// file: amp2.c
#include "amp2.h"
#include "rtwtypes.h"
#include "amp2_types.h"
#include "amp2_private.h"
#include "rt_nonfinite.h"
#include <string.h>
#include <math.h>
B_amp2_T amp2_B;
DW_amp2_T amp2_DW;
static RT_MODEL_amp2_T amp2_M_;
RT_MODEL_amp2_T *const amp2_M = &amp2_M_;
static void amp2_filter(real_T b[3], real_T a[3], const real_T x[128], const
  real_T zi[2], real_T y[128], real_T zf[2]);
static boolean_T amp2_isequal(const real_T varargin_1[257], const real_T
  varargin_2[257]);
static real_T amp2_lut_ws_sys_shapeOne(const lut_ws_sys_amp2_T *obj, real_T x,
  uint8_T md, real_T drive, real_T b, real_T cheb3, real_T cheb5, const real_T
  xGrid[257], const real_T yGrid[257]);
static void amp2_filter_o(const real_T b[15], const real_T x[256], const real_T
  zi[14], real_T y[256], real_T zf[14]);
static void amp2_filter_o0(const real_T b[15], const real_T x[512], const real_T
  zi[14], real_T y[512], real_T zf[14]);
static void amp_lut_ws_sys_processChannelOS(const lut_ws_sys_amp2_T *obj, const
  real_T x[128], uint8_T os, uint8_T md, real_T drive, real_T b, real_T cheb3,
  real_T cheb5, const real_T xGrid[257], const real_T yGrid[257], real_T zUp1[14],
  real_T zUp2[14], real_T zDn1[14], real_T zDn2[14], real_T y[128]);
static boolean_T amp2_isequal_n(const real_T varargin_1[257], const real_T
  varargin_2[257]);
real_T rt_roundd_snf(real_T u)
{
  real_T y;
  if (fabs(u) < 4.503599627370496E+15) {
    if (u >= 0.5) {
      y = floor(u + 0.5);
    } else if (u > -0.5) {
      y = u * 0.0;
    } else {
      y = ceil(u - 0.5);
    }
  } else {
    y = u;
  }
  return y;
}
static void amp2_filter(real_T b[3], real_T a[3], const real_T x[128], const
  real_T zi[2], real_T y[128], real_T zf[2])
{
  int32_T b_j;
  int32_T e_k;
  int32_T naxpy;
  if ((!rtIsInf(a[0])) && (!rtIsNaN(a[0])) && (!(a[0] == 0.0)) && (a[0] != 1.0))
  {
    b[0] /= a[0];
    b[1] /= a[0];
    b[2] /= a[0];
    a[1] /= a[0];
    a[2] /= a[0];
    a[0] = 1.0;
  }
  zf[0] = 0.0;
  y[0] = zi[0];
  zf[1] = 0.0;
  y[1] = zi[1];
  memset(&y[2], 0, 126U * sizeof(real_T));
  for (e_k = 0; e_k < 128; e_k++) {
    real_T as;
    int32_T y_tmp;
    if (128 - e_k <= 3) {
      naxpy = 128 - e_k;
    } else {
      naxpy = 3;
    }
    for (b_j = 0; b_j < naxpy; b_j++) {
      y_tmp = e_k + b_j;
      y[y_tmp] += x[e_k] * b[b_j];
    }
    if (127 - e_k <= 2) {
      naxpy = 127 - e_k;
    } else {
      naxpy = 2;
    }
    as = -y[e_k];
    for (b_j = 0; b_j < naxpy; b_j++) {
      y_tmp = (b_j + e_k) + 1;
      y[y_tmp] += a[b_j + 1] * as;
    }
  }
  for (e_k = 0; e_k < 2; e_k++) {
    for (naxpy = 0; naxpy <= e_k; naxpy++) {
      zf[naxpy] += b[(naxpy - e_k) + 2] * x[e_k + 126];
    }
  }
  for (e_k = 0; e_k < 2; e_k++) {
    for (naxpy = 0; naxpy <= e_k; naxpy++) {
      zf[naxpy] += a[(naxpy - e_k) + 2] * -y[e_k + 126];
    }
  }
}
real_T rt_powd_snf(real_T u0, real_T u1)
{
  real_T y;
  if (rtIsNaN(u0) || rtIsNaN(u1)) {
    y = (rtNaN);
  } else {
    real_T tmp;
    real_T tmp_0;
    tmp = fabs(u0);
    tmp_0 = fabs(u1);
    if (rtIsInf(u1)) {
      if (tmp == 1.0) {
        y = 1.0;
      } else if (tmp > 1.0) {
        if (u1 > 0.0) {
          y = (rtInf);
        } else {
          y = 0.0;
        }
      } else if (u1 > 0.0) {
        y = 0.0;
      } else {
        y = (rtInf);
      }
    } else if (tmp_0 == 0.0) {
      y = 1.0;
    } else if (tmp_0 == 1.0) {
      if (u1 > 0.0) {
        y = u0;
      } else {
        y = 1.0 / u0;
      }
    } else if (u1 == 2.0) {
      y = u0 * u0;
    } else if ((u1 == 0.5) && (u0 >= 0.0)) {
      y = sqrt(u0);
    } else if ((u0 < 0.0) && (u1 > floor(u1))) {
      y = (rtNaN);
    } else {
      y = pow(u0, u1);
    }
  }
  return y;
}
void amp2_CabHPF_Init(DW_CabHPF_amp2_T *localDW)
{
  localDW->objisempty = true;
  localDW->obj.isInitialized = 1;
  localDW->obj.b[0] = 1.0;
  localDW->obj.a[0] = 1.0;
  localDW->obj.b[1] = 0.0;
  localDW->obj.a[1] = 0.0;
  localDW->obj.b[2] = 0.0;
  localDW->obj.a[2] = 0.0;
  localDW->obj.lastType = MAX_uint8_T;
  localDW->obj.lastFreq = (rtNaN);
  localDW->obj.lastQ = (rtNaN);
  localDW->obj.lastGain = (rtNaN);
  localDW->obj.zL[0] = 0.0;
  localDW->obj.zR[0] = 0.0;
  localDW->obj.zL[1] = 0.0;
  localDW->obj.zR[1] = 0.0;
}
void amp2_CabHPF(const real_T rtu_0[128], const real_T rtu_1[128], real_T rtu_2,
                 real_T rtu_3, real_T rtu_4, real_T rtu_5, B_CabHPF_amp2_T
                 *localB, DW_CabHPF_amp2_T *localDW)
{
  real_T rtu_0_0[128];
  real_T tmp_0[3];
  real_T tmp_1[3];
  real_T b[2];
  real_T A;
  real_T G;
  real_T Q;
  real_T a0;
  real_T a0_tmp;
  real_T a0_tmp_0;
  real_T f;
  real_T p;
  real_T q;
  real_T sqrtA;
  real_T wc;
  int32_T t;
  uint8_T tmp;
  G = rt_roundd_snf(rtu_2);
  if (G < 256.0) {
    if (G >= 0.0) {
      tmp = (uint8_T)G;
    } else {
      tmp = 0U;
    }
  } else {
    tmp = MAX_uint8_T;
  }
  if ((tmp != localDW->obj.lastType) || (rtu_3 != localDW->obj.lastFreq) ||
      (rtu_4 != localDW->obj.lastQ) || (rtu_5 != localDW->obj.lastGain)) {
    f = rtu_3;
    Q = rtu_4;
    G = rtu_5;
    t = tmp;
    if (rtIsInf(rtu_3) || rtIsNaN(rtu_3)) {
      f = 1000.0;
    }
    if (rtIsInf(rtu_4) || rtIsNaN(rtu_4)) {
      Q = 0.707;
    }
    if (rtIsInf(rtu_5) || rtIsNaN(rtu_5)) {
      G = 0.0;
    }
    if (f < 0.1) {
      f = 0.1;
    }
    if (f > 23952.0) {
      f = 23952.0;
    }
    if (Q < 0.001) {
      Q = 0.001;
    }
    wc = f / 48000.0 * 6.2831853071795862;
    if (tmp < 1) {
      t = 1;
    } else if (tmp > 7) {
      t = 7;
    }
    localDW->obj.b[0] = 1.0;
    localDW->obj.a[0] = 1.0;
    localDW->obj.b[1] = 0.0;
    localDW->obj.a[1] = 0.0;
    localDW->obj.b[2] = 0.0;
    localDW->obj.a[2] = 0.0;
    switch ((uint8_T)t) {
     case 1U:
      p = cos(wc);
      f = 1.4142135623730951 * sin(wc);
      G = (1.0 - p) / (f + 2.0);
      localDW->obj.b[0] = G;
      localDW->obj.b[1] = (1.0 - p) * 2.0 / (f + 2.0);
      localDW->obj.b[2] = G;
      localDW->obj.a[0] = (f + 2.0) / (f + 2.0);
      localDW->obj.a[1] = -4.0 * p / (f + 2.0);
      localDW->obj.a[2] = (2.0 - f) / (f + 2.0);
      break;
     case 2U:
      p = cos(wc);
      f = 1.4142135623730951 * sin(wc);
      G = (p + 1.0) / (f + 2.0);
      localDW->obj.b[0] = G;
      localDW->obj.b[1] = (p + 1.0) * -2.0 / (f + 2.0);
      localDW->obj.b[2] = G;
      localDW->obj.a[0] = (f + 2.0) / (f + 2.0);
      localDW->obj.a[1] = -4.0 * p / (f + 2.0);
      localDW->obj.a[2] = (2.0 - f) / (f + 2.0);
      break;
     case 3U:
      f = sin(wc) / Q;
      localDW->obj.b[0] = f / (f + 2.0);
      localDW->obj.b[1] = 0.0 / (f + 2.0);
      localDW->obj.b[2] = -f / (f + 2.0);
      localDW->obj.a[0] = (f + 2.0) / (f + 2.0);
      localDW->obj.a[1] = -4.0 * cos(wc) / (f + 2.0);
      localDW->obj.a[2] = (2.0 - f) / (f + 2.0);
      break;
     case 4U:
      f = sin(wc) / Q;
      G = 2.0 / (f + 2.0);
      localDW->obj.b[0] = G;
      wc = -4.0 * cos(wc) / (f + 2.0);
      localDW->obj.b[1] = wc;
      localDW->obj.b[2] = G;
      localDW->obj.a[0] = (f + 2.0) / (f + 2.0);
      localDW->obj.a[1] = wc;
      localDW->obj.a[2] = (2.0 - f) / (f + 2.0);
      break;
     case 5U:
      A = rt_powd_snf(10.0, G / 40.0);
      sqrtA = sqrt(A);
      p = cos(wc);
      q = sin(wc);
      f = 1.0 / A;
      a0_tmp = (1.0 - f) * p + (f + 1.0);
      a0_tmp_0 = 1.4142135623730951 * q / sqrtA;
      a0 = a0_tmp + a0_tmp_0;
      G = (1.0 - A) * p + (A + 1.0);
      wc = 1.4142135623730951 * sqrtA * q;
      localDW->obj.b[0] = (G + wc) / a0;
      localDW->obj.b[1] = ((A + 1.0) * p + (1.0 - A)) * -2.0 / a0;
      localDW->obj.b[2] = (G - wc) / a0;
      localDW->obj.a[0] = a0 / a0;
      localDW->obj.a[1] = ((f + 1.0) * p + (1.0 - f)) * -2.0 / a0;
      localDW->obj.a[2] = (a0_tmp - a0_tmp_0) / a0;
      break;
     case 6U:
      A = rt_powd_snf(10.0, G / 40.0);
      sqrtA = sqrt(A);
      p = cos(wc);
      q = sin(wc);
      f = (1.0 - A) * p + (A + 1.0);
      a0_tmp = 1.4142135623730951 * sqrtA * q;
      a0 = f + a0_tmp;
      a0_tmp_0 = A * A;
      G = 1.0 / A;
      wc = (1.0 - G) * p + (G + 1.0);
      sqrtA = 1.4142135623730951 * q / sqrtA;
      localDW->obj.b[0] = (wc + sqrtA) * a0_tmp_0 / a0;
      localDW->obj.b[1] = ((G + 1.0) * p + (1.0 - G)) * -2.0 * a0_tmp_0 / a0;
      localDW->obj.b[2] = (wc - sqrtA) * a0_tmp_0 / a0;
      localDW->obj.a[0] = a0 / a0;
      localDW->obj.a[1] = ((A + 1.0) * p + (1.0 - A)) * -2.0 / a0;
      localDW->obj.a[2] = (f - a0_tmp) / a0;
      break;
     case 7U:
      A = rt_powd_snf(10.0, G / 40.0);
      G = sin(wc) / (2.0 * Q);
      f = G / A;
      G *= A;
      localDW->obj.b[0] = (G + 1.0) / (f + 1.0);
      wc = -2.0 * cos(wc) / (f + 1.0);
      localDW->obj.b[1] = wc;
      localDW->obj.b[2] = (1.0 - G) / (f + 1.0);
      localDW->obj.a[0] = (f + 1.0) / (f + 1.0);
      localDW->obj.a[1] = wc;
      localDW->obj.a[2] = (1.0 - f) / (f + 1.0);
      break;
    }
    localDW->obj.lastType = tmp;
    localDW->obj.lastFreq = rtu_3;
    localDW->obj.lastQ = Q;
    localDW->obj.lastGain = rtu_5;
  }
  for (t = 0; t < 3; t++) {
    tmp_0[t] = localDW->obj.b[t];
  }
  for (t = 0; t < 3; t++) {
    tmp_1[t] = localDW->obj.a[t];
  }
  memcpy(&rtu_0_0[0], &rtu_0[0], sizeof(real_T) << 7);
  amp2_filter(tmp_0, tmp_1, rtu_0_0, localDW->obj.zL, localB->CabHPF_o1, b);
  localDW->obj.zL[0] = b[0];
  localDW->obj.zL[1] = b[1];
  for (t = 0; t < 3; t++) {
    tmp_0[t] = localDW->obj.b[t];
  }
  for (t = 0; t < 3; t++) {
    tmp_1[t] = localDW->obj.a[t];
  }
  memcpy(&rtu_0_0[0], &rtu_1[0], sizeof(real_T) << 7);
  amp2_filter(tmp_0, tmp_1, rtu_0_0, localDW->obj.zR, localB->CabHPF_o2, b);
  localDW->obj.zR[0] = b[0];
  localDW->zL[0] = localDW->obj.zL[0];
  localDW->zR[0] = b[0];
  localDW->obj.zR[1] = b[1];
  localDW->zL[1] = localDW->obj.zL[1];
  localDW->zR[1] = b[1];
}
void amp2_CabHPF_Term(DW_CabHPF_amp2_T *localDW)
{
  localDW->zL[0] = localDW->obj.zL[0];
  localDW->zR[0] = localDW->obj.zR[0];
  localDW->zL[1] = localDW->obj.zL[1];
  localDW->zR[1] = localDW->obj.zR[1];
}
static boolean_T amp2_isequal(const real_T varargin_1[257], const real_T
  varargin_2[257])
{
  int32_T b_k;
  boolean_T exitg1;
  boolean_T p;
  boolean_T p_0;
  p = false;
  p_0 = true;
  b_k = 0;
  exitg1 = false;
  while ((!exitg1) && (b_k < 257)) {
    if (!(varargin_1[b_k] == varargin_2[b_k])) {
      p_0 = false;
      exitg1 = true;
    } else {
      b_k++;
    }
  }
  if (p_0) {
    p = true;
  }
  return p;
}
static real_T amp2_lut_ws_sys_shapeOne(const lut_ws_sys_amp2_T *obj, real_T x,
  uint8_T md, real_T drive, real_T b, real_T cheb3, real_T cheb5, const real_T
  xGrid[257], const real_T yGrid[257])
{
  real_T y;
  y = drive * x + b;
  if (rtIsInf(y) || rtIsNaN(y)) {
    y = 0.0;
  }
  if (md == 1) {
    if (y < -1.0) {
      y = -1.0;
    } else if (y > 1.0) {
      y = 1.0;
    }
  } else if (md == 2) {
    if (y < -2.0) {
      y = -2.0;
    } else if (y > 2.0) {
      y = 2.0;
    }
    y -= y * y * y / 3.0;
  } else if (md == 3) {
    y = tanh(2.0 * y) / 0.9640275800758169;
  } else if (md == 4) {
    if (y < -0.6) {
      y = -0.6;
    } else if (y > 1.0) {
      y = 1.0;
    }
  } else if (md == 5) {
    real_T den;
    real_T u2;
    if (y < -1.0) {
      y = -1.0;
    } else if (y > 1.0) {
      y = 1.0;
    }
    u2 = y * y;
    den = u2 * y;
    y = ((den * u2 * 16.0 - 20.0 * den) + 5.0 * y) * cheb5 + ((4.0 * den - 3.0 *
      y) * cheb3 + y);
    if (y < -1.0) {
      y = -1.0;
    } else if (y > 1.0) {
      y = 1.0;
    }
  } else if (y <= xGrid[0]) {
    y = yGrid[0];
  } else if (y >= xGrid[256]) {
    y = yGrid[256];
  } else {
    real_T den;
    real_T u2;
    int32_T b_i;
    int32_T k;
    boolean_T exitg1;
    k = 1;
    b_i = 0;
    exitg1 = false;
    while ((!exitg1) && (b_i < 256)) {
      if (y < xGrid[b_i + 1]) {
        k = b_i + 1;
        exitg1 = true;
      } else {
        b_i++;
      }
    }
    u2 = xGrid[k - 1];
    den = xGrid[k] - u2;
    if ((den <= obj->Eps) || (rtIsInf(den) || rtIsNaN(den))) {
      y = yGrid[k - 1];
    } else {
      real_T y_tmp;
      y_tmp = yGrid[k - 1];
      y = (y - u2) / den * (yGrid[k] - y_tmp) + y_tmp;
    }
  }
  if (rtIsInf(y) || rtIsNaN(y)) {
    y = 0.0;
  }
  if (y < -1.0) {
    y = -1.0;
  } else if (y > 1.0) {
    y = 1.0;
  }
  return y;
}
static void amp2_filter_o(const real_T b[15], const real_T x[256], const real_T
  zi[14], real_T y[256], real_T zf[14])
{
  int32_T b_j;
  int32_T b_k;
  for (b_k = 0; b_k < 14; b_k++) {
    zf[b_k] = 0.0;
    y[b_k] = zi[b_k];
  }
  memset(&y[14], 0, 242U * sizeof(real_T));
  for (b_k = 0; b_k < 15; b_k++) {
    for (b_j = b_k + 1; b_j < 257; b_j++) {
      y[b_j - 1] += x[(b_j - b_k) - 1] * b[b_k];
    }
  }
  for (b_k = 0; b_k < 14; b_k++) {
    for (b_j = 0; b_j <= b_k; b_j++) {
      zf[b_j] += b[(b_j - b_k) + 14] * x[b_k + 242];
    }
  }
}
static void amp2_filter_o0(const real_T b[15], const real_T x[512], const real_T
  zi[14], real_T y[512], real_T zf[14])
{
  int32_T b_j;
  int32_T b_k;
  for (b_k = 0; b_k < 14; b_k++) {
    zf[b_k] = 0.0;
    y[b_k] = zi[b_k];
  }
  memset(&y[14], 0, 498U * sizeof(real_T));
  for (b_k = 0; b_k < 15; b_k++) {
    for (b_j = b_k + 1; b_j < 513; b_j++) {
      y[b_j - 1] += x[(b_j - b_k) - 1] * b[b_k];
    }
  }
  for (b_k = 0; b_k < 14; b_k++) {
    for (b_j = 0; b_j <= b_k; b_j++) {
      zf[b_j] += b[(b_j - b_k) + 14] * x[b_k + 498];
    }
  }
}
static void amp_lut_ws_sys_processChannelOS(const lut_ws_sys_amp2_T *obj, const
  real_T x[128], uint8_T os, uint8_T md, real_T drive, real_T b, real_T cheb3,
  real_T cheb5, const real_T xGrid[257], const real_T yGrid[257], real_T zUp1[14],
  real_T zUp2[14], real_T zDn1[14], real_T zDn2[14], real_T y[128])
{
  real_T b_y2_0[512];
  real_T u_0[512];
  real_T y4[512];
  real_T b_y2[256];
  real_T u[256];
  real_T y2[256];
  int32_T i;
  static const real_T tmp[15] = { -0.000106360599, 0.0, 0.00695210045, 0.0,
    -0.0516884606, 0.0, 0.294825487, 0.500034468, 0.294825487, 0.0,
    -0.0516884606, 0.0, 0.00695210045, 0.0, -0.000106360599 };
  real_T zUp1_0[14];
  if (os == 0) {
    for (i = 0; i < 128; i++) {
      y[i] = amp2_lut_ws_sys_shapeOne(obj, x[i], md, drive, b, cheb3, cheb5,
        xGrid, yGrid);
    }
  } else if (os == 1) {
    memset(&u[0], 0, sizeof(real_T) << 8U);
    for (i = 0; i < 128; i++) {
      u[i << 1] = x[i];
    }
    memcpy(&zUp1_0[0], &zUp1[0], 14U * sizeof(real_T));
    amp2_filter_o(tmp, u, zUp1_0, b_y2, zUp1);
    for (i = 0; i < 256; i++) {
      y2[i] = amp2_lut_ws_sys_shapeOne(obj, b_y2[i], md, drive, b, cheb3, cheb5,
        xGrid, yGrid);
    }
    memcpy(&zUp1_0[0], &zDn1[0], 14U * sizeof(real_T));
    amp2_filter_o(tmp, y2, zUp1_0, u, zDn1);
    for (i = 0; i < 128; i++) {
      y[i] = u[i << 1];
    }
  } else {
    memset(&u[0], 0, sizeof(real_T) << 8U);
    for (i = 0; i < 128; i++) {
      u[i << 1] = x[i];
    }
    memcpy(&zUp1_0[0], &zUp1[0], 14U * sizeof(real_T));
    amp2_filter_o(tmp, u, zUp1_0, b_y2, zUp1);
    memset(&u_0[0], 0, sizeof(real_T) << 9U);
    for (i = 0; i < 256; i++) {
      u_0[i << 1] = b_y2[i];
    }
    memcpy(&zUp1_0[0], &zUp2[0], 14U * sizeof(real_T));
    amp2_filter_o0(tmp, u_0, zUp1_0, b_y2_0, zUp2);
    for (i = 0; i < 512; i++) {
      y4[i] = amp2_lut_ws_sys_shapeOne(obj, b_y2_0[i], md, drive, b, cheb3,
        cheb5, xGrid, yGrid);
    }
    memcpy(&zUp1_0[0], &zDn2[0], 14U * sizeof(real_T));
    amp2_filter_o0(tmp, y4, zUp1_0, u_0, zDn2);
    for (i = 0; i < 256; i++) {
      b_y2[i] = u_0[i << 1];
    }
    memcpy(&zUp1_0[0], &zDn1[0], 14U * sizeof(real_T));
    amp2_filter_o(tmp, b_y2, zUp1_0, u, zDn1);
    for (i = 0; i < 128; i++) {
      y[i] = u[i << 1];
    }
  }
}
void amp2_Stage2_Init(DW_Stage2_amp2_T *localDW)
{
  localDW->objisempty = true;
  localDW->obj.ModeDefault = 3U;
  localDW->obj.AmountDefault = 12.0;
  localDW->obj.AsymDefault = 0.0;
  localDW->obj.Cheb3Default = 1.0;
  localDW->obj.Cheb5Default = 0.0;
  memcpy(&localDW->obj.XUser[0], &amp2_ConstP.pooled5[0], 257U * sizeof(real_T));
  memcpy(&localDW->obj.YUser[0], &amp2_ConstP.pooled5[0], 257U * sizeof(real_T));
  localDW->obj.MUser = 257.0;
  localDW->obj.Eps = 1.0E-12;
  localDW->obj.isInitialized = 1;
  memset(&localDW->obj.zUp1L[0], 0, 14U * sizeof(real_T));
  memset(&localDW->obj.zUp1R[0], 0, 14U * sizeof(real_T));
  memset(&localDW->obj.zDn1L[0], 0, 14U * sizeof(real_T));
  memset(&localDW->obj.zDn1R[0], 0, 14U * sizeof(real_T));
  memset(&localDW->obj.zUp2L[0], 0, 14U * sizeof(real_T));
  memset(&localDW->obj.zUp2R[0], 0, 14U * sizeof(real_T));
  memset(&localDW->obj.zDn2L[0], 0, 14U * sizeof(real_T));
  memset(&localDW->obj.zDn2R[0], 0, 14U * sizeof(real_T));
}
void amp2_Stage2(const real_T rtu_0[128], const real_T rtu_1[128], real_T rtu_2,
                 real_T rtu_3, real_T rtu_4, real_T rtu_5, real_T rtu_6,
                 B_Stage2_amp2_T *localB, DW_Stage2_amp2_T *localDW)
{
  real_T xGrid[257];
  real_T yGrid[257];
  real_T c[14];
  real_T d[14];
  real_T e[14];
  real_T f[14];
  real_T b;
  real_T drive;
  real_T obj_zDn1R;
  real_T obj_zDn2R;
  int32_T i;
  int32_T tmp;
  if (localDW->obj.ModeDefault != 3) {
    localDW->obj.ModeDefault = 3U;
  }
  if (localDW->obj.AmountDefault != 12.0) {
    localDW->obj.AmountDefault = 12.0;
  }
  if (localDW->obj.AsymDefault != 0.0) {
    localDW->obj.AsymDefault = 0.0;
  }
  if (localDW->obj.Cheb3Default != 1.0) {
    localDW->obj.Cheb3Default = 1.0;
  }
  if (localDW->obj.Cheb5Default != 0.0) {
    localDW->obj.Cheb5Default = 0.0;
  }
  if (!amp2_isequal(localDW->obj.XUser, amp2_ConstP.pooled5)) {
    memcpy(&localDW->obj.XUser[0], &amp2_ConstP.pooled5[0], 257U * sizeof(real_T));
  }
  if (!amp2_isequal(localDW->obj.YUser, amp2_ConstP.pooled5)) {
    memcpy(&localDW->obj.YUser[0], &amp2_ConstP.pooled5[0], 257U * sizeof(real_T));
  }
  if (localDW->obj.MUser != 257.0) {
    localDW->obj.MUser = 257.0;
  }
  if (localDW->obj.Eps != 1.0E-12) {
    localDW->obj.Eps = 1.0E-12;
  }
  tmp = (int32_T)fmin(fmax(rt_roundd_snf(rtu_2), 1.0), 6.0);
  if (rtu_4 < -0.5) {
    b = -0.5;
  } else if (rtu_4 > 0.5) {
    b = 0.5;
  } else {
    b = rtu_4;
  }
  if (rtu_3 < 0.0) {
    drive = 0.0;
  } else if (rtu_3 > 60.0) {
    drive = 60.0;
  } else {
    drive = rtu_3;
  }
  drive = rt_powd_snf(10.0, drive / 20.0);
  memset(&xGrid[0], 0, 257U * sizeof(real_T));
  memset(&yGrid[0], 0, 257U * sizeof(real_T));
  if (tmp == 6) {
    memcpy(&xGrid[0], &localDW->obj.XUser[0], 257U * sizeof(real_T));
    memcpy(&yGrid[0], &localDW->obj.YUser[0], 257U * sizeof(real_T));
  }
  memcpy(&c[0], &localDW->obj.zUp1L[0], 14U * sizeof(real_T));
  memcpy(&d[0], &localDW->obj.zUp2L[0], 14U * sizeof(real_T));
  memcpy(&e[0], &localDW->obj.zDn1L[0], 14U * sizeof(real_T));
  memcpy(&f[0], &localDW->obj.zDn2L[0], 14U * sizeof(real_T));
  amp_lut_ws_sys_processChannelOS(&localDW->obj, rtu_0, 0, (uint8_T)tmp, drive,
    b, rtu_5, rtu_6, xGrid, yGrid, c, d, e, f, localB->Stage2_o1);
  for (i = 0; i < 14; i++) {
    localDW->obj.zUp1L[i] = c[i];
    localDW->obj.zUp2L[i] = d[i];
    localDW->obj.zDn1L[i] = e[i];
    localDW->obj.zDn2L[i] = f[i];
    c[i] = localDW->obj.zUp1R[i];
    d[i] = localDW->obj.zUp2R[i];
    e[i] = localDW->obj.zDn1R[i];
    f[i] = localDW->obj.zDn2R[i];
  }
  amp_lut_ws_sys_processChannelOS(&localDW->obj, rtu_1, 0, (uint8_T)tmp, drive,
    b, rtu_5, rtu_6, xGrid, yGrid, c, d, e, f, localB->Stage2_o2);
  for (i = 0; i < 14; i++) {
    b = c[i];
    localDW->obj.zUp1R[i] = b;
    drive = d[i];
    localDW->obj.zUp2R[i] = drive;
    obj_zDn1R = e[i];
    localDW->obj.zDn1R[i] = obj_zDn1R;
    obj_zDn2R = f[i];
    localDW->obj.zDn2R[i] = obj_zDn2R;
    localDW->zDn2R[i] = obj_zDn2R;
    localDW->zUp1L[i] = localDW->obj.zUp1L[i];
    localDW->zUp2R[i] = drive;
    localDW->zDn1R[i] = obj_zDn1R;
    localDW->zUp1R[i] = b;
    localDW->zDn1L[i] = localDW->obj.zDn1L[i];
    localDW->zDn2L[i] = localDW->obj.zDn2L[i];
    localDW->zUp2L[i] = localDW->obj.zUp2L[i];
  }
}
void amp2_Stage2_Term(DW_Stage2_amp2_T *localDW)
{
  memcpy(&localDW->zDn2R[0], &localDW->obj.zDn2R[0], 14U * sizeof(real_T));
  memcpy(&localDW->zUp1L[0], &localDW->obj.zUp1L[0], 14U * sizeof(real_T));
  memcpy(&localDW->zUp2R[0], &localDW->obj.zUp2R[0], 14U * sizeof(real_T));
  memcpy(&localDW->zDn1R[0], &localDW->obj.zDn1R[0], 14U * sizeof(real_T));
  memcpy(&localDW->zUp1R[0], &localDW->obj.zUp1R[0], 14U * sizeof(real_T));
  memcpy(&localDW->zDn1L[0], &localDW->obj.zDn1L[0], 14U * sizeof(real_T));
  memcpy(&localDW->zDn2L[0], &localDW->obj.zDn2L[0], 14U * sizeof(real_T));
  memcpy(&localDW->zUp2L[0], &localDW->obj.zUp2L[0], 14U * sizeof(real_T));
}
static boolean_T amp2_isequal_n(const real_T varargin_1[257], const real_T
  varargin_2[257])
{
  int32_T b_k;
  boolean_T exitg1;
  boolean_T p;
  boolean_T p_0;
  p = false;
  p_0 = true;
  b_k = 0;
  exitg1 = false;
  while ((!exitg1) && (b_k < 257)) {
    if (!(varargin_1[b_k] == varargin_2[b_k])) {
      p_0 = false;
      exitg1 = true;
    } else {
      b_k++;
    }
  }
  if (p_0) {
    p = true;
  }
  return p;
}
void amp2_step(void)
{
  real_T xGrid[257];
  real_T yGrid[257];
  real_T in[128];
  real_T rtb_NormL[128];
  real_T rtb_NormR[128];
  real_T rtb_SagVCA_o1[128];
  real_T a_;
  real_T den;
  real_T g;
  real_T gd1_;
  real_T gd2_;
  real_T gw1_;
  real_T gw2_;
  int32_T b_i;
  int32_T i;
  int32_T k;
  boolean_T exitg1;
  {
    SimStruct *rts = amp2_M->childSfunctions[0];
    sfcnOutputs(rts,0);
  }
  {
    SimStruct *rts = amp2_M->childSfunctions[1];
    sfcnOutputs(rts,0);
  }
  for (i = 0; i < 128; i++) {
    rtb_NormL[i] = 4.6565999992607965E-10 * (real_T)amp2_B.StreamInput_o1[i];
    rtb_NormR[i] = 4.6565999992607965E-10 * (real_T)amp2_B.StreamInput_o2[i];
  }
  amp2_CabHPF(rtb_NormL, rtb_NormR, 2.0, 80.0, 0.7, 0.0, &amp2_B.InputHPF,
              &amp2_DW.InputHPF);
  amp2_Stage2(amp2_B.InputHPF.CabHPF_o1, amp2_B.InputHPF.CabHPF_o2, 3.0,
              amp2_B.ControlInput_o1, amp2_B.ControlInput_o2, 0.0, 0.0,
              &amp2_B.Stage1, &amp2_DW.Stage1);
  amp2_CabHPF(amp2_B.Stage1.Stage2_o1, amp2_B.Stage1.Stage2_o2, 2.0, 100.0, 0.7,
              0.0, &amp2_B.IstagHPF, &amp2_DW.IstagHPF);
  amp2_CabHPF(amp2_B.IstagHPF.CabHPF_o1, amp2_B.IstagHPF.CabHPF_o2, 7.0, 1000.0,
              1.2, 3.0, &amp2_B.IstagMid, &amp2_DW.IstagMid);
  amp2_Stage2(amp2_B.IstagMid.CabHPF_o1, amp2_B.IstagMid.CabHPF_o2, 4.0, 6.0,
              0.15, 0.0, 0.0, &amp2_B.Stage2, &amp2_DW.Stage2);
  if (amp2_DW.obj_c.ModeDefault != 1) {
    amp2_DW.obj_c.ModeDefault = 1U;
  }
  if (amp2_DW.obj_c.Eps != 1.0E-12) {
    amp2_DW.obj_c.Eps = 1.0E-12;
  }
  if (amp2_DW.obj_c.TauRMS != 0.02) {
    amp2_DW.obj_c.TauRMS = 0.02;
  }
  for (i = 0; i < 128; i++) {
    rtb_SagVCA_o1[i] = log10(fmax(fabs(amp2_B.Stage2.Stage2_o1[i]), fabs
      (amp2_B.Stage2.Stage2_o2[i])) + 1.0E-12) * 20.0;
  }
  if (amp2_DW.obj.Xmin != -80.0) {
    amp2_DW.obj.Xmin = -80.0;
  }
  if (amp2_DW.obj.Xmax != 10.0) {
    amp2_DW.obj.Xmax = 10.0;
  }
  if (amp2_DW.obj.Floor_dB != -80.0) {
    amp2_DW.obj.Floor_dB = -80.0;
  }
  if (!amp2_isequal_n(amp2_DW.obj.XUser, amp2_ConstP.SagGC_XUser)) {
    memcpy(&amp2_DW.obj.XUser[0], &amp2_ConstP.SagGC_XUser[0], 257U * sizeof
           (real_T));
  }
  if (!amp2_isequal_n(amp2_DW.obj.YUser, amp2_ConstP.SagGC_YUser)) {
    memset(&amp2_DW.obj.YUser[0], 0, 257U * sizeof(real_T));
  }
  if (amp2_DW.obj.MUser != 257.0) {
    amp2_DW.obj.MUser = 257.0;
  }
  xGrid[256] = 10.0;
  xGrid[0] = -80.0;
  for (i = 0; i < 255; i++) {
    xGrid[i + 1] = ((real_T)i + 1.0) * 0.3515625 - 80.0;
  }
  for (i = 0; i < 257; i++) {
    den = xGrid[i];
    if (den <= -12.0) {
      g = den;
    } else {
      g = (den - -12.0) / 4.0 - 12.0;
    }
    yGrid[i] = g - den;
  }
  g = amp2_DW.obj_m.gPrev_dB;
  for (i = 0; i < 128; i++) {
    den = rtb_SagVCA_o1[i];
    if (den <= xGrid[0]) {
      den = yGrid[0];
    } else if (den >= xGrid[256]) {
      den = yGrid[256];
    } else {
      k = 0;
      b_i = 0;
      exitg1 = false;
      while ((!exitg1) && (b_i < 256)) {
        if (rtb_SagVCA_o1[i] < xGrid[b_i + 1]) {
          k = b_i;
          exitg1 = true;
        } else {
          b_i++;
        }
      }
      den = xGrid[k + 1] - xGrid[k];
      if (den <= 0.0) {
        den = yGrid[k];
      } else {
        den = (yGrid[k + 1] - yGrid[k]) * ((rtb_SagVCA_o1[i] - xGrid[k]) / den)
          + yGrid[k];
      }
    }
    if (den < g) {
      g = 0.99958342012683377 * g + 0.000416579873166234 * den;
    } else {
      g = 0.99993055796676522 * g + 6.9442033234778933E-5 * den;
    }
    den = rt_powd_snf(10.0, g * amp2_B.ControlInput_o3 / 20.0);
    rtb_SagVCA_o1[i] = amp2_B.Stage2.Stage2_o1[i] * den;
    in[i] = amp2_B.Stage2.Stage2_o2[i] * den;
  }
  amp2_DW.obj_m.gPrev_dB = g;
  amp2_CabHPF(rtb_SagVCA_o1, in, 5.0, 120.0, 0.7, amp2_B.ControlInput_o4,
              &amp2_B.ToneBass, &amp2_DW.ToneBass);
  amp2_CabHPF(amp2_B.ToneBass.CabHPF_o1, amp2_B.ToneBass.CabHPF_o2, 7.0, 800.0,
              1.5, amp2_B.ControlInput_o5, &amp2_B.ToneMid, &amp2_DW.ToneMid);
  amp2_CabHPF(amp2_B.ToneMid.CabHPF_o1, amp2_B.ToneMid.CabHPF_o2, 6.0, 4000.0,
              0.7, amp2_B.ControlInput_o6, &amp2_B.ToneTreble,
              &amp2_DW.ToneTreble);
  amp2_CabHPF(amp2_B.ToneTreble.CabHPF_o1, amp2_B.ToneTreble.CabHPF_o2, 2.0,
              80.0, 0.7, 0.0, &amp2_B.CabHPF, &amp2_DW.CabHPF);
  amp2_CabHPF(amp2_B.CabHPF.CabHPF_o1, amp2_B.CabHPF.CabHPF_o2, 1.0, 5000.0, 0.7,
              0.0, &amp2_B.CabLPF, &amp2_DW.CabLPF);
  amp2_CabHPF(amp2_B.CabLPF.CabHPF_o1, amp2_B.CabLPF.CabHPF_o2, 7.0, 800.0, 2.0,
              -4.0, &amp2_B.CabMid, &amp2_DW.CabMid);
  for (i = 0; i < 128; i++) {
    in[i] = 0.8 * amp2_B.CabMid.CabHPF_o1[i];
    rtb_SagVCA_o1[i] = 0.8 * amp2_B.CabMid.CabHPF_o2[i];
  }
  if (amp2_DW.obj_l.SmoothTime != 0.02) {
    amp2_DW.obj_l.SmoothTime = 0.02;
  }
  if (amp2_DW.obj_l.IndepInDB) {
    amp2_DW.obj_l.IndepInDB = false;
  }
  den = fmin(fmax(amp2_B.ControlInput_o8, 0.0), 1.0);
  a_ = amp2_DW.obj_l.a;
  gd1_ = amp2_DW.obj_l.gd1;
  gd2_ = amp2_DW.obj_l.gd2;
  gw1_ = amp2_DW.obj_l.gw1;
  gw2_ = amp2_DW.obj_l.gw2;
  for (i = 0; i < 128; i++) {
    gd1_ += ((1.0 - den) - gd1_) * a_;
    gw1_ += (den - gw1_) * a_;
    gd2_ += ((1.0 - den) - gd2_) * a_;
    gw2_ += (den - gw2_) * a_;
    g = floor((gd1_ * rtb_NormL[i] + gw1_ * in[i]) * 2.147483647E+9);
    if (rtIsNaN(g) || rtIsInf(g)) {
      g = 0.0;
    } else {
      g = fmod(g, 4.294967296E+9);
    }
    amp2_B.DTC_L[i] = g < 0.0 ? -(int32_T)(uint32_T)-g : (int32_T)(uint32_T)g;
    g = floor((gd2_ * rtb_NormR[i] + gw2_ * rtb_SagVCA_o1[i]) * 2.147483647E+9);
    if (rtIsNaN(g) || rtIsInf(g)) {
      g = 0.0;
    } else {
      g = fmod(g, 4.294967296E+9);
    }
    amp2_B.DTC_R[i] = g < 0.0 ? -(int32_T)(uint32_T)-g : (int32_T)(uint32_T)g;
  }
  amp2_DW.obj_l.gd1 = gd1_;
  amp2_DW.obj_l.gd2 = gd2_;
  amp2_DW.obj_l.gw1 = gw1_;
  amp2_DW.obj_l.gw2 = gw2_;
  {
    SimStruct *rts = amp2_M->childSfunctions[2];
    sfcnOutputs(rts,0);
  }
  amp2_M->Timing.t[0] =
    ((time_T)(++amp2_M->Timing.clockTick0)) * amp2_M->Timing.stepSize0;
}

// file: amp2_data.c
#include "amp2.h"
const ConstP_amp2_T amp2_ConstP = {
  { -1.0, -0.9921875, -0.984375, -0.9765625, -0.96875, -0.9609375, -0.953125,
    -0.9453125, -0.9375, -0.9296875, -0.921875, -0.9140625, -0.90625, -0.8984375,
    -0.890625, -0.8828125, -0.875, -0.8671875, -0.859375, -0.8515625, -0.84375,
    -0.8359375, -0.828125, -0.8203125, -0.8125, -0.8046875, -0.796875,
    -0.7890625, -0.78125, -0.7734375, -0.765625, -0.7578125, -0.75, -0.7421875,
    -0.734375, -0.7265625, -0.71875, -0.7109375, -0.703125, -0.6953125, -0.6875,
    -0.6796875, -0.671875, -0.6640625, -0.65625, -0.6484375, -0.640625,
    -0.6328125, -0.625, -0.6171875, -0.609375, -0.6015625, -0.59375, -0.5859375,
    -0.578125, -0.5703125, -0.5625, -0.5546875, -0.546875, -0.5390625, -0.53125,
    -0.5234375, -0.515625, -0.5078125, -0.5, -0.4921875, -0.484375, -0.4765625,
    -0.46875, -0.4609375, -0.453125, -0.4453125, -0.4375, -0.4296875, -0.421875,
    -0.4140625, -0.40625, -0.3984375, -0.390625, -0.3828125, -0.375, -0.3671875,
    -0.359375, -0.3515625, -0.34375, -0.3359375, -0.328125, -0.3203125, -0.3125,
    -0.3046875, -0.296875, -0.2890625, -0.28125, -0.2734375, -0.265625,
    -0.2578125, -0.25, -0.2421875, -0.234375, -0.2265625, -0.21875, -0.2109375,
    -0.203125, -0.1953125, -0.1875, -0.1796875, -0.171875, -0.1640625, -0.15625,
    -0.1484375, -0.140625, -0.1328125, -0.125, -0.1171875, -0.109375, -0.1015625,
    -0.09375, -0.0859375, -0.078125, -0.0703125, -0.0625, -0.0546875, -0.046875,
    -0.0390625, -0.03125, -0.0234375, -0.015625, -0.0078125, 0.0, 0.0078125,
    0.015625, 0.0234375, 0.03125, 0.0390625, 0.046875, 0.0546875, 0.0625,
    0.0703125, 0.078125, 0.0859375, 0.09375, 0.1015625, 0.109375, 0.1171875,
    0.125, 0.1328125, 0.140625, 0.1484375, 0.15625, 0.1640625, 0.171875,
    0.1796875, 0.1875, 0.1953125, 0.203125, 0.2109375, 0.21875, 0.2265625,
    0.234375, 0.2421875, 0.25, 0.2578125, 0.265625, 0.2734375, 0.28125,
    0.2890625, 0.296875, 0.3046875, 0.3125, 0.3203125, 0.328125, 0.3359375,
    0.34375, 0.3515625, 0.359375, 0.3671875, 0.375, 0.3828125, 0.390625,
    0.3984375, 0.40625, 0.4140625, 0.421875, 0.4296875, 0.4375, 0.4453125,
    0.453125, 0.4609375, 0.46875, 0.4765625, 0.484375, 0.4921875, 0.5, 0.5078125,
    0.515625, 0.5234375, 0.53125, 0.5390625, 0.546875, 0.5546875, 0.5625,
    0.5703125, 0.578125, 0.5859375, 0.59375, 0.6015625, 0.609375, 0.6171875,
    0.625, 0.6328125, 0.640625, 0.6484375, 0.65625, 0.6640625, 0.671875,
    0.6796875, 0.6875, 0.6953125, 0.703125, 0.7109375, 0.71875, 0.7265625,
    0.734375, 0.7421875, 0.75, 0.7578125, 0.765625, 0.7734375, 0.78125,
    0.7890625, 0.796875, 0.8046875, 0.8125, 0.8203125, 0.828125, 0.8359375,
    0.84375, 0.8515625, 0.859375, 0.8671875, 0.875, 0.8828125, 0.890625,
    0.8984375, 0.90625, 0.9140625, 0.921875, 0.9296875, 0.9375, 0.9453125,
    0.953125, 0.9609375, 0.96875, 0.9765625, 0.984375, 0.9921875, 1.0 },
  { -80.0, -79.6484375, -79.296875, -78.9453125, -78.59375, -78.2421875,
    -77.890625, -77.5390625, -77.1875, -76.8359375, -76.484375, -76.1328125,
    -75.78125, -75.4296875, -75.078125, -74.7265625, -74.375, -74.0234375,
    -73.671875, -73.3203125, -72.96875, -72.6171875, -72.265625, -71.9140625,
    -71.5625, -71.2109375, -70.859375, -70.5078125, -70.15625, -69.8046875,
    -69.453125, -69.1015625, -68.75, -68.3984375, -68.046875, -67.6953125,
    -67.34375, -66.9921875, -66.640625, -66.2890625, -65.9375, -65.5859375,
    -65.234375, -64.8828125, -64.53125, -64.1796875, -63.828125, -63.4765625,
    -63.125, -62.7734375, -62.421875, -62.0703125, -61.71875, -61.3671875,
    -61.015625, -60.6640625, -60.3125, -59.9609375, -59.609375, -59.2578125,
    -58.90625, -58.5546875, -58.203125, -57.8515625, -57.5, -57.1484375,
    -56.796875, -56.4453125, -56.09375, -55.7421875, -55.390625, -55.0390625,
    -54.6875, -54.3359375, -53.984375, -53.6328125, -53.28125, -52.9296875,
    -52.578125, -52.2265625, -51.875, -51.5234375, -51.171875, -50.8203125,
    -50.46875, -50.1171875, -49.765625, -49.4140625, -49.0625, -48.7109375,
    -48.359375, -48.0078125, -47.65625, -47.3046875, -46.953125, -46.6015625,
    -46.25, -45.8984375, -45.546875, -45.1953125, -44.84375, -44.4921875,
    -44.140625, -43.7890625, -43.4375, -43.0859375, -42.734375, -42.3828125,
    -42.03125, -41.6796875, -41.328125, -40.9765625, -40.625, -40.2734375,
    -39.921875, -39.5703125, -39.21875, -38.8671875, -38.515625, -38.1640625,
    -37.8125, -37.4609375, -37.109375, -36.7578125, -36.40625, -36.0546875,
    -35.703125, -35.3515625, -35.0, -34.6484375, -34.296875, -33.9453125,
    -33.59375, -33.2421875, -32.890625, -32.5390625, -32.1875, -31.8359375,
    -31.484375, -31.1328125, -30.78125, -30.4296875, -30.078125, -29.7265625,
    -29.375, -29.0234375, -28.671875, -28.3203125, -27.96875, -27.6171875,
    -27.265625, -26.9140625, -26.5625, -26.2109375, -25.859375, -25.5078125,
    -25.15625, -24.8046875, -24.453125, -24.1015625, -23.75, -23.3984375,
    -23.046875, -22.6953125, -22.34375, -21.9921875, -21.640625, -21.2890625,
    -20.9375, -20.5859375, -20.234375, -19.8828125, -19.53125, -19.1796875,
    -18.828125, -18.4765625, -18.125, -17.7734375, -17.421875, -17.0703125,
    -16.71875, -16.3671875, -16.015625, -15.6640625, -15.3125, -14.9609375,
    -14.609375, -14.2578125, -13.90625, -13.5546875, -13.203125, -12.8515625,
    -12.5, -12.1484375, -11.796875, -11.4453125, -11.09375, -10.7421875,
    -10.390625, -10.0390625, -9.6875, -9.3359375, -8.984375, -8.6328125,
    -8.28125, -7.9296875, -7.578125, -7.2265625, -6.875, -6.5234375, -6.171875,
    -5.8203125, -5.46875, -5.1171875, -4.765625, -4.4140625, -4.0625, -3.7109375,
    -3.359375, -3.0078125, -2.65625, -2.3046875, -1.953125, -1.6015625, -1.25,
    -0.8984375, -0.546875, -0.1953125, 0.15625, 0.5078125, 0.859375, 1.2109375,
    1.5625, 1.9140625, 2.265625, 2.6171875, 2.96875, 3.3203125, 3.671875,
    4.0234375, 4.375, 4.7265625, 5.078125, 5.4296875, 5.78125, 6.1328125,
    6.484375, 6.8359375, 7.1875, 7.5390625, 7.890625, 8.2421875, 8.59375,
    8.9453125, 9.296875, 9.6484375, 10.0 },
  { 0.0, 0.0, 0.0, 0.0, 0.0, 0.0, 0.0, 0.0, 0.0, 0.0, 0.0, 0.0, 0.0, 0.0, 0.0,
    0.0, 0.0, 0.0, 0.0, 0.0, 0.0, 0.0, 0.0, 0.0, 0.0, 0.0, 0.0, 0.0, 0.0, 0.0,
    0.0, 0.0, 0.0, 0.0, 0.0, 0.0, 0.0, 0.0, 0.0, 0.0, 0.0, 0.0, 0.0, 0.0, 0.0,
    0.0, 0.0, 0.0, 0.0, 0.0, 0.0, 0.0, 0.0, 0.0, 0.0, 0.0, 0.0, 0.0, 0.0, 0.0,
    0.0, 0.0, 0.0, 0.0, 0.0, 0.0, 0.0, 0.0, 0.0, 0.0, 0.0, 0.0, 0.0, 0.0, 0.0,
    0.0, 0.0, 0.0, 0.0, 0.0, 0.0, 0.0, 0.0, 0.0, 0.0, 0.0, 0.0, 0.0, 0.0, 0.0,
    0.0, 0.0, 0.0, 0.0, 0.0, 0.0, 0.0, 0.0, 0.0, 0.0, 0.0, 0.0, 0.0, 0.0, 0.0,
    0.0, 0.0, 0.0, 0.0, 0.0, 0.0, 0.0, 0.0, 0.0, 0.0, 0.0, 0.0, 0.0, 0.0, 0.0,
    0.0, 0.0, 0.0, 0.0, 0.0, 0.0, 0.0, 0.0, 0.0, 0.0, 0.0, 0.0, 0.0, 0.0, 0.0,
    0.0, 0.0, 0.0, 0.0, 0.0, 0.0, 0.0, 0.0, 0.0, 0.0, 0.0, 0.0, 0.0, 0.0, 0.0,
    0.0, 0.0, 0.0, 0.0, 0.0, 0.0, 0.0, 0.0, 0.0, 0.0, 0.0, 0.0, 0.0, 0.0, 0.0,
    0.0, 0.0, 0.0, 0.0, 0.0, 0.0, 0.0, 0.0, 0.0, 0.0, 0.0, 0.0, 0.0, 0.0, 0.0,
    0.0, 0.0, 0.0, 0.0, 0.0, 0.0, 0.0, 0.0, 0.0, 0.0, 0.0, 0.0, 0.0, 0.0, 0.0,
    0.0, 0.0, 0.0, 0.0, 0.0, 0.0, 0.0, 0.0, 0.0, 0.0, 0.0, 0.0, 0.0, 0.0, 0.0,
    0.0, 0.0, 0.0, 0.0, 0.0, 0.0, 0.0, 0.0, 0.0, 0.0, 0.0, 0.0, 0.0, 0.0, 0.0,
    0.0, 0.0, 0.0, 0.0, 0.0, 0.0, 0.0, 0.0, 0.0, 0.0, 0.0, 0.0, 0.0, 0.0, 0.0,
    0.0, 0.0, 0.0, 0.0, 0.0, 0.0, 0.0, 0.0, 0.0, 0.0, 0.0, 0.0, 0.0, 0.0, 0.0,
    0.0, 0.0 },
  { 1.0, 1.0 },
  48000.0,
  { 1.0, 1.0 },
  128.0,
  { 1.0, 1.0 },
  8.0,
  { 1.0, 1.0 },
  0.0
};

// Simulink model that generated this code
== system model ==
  SFunction#1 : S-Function  FunctionName=stream_out  <- 1: DTC_L, 2: DTC_R
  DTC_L : DataTypeConversion  <- 1: Gain#1
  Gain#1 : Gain  Gain=2147483647  <- 1: MATLABSystem#1
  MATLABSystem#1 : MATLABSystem  N=128  <- 1: NormL, 2: NormR, 3: Gain#2, 4: Gain#3, 5: ControlInput/8
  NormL : Gain  Gain=4.6566e-10  <- 1: StreamInput
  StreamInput : S-Function  FunctionName=stream_in
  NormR : Gain  Gain=4.6566e-10  <- 1: StreamInput/2
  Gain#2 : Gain  Gain=0.8  <- 1: CabMid
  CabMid : MATLABSystem  N=128  <- 1: CabLPF, 2: CabLPF/2, 3: Constant#1, 4: Constant#2, 5: Constant#3, 6: Constant#4
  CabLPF : MATLABSystem  N=128  <- 1: CabHPF, 2: CabHPF/2, 3: Constant#5, 4: Constant#6, 5: Constant#7, 6: Constant#8
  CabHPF : MATLABSystem  N=128  <- 1: ToneTreble, 2: ToneTreble/2, 3: Constant#9, 4: Constant#10, 5: Constant#11, 6: Constant#12
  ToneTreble : MATLABSystem  N=128  <- 1: ToneMid, 2: ToneMid/2, 3: Constant#13, 4: Constant#14, 5: Constant#15, 6: ControlInput/6
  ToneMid : MATLABSystem  N=128  <- 1: ToneBass, 2: ToneBass/2, 3: Constant#16, 4: Constant#17, 5: Constant#18, 6: ControlInput/5
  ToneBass : MATLABSystem  N=128  <- 1: SagVCA, 2: SagVCA/2, 3: Constant#19, 4: Constant#20, 5: Constant#21, 6: ControlInput/4
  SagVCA : MATLABSystem  N=128  <- 1: Stage2, 2: Stage2/2, 3: Product#1, 4: Constant#22
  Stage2 : MATLABSystem  N=128  <- 1: IstagMid, 2: IstagMid/2, 3: Constant#23, 4: Constant#24, 5: Constant#25, 6: Constant#26, 7: Constant#27
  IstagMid : MATLABSystem  N=128  <- 1: IstagHPF, 2: IstagHPF/2, 3: Constant#28, 4: Constant#29, 5: Constant#30, 6: Constant#31
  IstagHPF : MATLABSystem  N=128  <- 1: Stage1, 2: Stage1/2, 3: Constant#32, 4: Constant#33, 5: Constant#34, 6: Constant#35
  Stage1 : MATLABSystem  N=128  <- 1: InputHPF, 2: InputHPF/2, 3: Constant#36, 4: ControlInput, 5: ControlInput/2, 6: Constant#37, 7: Constant#38
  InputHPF : MATLABSystem  N=128  <- 1: NormL, 2: NormR, 3: Constant#39, 4: Constant#40, 5: Constant#41, 6: Constant#42
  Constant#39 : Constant  Value=2
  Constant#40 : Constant  Value=80
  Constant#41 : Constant  Value=0.7
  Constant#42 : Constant  Value=0
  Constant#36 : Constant  Value=3
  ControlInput : S-Function  FunctionName=ctrl_in
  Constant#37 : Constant  Value=0
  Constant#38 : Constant  Value=0
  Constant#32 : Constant  Value=2
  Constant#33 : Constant  Value=100
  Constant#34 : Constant  Value=0.7
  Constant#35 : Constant  Value=0
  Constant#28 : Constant  Value=7
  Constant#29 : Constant  Value=1000
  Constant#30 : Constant  Value=1.2
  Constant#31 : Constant  Value=3
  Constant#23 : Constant  Value=4
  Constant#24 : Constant  Value=6
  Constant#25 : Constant  Value=0.15
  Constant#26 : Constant  Value=0
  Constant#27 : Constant  Value=0
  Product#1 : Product  Inputs=**  <- 1: MATLABSystem#2, 2: ControlInput/3
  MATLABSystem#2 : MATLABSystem  N=128  <- 1: SagGC, 2: Constant#43, 3: Constant#44
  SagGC : MATLABSystem  N=128  <- 1: MATLABSystem#3, 2: Constant#45, 3: Constant#46, 4: Constant#47, 5: Constant#48, 6: Constant#49
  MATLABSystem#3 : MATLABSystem  N=128  <- 1: Stage2, 2: Stage2/2, 3: Constant#50
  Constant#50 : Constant
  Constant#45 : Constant
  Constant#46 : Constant  Value=-12
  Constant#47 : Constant  Value=4
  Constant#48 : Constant  Value=6
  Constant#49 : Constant  Value=0
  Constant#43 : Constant  Value=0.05
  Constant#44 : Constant  Value=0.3
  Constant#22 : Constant
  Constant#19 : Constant  Value=5
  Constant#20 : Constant  Value=120
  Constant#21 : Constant  Value=0.7
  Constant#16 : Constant  Value=7
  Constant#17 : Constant  Value=800
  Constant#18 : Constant  Value=1.5
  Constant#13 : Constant  Value=6
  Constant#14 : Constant  Value=4000
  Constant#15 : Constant  Value=0.7
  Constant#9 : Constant  Value=2
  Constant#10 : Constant  Value=80
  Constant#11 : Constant  Value=0.7
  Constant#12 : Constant  Value=0
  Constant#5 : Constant
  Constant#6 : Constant  Value=5000
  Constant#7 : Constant  Value=0.7
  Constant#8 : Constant  Value=0
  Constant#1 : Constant  Value=7
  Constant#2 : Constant  Value=800
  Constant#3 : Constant  Value=2
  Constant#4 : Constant  Value=-4
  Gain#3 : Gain  Gain=0.8  <- 1: CabMid/2
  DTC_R : DataTypeConversion  <- 1: Gain#4
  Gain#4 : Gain  Gain=2147483647  <- 1: MATLABSystem#1/2
